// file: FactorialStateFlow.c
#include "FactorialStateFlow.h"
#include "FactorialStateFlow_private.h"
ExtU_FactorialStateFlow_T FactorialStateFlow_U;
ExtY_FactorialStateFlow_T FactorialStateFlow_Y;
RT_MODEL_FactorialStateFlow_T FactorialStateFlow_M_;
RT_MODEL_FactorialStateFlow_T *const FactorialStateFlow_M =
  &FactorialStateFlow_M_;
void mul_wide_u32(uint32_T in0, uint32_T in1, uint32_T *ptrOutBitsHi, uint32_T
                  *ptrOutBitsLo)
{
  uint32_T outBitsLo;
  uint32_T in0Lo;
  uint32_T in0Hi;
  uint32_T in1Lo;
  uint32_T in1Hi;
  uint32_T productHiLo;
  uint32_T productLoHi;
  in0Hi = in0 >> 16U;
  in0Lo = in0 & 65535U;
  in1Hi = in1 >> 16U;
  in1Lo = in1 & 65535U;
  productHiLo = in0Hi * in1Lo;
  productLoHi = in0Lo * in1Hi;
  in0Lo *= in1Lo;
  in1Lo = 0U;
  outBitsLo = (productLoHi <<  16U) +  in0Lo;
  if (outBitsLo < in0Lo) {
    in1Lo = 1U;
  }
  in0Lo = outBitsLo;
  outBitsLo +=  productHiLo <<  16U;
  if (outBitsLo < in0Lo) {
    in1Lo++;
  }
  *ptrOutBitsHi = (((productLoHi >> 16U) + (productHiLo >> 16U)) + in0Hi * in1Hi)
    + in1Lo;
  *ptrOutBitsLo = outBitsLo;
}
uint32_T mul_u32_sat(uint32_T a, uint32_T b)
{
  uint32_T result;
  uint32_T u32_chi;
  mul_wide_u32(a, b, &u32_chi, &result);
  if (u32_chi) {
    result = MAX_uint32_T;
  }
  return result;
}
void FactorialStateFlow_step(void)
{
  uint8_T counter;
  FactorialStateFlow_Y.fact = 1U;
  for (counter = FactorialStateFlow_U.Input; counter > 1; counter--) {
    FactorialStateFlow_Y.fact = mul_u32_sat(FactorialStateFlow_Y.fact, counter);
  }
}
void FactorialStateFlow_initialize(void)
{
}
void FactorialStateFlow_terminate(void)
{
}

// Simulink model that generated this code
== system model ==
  Input : Inport
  fact : Outport  <- 1: Stateflowchart#1
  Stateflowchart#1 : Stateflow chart  <- 1: Input
== stateflow chart Stateflowchart#1 ==
  (default) -> (junction 8)
  (junction 8) -> (junction 10) : {fact=1; counter=var;}
  (junction 10) -> (junction 9) [order 1] : [counter>1]
  (junction 12) -> (junction 10)
  (junction 9) -> (junction 11) : {fact=fact*counter}
  (junction 10) -> (junction 13) [order 2]
  (junction 11) -> (junction 12) : {counter = counter - 1;}
  data: var input uint8; fact output uint32; counter local uint8
